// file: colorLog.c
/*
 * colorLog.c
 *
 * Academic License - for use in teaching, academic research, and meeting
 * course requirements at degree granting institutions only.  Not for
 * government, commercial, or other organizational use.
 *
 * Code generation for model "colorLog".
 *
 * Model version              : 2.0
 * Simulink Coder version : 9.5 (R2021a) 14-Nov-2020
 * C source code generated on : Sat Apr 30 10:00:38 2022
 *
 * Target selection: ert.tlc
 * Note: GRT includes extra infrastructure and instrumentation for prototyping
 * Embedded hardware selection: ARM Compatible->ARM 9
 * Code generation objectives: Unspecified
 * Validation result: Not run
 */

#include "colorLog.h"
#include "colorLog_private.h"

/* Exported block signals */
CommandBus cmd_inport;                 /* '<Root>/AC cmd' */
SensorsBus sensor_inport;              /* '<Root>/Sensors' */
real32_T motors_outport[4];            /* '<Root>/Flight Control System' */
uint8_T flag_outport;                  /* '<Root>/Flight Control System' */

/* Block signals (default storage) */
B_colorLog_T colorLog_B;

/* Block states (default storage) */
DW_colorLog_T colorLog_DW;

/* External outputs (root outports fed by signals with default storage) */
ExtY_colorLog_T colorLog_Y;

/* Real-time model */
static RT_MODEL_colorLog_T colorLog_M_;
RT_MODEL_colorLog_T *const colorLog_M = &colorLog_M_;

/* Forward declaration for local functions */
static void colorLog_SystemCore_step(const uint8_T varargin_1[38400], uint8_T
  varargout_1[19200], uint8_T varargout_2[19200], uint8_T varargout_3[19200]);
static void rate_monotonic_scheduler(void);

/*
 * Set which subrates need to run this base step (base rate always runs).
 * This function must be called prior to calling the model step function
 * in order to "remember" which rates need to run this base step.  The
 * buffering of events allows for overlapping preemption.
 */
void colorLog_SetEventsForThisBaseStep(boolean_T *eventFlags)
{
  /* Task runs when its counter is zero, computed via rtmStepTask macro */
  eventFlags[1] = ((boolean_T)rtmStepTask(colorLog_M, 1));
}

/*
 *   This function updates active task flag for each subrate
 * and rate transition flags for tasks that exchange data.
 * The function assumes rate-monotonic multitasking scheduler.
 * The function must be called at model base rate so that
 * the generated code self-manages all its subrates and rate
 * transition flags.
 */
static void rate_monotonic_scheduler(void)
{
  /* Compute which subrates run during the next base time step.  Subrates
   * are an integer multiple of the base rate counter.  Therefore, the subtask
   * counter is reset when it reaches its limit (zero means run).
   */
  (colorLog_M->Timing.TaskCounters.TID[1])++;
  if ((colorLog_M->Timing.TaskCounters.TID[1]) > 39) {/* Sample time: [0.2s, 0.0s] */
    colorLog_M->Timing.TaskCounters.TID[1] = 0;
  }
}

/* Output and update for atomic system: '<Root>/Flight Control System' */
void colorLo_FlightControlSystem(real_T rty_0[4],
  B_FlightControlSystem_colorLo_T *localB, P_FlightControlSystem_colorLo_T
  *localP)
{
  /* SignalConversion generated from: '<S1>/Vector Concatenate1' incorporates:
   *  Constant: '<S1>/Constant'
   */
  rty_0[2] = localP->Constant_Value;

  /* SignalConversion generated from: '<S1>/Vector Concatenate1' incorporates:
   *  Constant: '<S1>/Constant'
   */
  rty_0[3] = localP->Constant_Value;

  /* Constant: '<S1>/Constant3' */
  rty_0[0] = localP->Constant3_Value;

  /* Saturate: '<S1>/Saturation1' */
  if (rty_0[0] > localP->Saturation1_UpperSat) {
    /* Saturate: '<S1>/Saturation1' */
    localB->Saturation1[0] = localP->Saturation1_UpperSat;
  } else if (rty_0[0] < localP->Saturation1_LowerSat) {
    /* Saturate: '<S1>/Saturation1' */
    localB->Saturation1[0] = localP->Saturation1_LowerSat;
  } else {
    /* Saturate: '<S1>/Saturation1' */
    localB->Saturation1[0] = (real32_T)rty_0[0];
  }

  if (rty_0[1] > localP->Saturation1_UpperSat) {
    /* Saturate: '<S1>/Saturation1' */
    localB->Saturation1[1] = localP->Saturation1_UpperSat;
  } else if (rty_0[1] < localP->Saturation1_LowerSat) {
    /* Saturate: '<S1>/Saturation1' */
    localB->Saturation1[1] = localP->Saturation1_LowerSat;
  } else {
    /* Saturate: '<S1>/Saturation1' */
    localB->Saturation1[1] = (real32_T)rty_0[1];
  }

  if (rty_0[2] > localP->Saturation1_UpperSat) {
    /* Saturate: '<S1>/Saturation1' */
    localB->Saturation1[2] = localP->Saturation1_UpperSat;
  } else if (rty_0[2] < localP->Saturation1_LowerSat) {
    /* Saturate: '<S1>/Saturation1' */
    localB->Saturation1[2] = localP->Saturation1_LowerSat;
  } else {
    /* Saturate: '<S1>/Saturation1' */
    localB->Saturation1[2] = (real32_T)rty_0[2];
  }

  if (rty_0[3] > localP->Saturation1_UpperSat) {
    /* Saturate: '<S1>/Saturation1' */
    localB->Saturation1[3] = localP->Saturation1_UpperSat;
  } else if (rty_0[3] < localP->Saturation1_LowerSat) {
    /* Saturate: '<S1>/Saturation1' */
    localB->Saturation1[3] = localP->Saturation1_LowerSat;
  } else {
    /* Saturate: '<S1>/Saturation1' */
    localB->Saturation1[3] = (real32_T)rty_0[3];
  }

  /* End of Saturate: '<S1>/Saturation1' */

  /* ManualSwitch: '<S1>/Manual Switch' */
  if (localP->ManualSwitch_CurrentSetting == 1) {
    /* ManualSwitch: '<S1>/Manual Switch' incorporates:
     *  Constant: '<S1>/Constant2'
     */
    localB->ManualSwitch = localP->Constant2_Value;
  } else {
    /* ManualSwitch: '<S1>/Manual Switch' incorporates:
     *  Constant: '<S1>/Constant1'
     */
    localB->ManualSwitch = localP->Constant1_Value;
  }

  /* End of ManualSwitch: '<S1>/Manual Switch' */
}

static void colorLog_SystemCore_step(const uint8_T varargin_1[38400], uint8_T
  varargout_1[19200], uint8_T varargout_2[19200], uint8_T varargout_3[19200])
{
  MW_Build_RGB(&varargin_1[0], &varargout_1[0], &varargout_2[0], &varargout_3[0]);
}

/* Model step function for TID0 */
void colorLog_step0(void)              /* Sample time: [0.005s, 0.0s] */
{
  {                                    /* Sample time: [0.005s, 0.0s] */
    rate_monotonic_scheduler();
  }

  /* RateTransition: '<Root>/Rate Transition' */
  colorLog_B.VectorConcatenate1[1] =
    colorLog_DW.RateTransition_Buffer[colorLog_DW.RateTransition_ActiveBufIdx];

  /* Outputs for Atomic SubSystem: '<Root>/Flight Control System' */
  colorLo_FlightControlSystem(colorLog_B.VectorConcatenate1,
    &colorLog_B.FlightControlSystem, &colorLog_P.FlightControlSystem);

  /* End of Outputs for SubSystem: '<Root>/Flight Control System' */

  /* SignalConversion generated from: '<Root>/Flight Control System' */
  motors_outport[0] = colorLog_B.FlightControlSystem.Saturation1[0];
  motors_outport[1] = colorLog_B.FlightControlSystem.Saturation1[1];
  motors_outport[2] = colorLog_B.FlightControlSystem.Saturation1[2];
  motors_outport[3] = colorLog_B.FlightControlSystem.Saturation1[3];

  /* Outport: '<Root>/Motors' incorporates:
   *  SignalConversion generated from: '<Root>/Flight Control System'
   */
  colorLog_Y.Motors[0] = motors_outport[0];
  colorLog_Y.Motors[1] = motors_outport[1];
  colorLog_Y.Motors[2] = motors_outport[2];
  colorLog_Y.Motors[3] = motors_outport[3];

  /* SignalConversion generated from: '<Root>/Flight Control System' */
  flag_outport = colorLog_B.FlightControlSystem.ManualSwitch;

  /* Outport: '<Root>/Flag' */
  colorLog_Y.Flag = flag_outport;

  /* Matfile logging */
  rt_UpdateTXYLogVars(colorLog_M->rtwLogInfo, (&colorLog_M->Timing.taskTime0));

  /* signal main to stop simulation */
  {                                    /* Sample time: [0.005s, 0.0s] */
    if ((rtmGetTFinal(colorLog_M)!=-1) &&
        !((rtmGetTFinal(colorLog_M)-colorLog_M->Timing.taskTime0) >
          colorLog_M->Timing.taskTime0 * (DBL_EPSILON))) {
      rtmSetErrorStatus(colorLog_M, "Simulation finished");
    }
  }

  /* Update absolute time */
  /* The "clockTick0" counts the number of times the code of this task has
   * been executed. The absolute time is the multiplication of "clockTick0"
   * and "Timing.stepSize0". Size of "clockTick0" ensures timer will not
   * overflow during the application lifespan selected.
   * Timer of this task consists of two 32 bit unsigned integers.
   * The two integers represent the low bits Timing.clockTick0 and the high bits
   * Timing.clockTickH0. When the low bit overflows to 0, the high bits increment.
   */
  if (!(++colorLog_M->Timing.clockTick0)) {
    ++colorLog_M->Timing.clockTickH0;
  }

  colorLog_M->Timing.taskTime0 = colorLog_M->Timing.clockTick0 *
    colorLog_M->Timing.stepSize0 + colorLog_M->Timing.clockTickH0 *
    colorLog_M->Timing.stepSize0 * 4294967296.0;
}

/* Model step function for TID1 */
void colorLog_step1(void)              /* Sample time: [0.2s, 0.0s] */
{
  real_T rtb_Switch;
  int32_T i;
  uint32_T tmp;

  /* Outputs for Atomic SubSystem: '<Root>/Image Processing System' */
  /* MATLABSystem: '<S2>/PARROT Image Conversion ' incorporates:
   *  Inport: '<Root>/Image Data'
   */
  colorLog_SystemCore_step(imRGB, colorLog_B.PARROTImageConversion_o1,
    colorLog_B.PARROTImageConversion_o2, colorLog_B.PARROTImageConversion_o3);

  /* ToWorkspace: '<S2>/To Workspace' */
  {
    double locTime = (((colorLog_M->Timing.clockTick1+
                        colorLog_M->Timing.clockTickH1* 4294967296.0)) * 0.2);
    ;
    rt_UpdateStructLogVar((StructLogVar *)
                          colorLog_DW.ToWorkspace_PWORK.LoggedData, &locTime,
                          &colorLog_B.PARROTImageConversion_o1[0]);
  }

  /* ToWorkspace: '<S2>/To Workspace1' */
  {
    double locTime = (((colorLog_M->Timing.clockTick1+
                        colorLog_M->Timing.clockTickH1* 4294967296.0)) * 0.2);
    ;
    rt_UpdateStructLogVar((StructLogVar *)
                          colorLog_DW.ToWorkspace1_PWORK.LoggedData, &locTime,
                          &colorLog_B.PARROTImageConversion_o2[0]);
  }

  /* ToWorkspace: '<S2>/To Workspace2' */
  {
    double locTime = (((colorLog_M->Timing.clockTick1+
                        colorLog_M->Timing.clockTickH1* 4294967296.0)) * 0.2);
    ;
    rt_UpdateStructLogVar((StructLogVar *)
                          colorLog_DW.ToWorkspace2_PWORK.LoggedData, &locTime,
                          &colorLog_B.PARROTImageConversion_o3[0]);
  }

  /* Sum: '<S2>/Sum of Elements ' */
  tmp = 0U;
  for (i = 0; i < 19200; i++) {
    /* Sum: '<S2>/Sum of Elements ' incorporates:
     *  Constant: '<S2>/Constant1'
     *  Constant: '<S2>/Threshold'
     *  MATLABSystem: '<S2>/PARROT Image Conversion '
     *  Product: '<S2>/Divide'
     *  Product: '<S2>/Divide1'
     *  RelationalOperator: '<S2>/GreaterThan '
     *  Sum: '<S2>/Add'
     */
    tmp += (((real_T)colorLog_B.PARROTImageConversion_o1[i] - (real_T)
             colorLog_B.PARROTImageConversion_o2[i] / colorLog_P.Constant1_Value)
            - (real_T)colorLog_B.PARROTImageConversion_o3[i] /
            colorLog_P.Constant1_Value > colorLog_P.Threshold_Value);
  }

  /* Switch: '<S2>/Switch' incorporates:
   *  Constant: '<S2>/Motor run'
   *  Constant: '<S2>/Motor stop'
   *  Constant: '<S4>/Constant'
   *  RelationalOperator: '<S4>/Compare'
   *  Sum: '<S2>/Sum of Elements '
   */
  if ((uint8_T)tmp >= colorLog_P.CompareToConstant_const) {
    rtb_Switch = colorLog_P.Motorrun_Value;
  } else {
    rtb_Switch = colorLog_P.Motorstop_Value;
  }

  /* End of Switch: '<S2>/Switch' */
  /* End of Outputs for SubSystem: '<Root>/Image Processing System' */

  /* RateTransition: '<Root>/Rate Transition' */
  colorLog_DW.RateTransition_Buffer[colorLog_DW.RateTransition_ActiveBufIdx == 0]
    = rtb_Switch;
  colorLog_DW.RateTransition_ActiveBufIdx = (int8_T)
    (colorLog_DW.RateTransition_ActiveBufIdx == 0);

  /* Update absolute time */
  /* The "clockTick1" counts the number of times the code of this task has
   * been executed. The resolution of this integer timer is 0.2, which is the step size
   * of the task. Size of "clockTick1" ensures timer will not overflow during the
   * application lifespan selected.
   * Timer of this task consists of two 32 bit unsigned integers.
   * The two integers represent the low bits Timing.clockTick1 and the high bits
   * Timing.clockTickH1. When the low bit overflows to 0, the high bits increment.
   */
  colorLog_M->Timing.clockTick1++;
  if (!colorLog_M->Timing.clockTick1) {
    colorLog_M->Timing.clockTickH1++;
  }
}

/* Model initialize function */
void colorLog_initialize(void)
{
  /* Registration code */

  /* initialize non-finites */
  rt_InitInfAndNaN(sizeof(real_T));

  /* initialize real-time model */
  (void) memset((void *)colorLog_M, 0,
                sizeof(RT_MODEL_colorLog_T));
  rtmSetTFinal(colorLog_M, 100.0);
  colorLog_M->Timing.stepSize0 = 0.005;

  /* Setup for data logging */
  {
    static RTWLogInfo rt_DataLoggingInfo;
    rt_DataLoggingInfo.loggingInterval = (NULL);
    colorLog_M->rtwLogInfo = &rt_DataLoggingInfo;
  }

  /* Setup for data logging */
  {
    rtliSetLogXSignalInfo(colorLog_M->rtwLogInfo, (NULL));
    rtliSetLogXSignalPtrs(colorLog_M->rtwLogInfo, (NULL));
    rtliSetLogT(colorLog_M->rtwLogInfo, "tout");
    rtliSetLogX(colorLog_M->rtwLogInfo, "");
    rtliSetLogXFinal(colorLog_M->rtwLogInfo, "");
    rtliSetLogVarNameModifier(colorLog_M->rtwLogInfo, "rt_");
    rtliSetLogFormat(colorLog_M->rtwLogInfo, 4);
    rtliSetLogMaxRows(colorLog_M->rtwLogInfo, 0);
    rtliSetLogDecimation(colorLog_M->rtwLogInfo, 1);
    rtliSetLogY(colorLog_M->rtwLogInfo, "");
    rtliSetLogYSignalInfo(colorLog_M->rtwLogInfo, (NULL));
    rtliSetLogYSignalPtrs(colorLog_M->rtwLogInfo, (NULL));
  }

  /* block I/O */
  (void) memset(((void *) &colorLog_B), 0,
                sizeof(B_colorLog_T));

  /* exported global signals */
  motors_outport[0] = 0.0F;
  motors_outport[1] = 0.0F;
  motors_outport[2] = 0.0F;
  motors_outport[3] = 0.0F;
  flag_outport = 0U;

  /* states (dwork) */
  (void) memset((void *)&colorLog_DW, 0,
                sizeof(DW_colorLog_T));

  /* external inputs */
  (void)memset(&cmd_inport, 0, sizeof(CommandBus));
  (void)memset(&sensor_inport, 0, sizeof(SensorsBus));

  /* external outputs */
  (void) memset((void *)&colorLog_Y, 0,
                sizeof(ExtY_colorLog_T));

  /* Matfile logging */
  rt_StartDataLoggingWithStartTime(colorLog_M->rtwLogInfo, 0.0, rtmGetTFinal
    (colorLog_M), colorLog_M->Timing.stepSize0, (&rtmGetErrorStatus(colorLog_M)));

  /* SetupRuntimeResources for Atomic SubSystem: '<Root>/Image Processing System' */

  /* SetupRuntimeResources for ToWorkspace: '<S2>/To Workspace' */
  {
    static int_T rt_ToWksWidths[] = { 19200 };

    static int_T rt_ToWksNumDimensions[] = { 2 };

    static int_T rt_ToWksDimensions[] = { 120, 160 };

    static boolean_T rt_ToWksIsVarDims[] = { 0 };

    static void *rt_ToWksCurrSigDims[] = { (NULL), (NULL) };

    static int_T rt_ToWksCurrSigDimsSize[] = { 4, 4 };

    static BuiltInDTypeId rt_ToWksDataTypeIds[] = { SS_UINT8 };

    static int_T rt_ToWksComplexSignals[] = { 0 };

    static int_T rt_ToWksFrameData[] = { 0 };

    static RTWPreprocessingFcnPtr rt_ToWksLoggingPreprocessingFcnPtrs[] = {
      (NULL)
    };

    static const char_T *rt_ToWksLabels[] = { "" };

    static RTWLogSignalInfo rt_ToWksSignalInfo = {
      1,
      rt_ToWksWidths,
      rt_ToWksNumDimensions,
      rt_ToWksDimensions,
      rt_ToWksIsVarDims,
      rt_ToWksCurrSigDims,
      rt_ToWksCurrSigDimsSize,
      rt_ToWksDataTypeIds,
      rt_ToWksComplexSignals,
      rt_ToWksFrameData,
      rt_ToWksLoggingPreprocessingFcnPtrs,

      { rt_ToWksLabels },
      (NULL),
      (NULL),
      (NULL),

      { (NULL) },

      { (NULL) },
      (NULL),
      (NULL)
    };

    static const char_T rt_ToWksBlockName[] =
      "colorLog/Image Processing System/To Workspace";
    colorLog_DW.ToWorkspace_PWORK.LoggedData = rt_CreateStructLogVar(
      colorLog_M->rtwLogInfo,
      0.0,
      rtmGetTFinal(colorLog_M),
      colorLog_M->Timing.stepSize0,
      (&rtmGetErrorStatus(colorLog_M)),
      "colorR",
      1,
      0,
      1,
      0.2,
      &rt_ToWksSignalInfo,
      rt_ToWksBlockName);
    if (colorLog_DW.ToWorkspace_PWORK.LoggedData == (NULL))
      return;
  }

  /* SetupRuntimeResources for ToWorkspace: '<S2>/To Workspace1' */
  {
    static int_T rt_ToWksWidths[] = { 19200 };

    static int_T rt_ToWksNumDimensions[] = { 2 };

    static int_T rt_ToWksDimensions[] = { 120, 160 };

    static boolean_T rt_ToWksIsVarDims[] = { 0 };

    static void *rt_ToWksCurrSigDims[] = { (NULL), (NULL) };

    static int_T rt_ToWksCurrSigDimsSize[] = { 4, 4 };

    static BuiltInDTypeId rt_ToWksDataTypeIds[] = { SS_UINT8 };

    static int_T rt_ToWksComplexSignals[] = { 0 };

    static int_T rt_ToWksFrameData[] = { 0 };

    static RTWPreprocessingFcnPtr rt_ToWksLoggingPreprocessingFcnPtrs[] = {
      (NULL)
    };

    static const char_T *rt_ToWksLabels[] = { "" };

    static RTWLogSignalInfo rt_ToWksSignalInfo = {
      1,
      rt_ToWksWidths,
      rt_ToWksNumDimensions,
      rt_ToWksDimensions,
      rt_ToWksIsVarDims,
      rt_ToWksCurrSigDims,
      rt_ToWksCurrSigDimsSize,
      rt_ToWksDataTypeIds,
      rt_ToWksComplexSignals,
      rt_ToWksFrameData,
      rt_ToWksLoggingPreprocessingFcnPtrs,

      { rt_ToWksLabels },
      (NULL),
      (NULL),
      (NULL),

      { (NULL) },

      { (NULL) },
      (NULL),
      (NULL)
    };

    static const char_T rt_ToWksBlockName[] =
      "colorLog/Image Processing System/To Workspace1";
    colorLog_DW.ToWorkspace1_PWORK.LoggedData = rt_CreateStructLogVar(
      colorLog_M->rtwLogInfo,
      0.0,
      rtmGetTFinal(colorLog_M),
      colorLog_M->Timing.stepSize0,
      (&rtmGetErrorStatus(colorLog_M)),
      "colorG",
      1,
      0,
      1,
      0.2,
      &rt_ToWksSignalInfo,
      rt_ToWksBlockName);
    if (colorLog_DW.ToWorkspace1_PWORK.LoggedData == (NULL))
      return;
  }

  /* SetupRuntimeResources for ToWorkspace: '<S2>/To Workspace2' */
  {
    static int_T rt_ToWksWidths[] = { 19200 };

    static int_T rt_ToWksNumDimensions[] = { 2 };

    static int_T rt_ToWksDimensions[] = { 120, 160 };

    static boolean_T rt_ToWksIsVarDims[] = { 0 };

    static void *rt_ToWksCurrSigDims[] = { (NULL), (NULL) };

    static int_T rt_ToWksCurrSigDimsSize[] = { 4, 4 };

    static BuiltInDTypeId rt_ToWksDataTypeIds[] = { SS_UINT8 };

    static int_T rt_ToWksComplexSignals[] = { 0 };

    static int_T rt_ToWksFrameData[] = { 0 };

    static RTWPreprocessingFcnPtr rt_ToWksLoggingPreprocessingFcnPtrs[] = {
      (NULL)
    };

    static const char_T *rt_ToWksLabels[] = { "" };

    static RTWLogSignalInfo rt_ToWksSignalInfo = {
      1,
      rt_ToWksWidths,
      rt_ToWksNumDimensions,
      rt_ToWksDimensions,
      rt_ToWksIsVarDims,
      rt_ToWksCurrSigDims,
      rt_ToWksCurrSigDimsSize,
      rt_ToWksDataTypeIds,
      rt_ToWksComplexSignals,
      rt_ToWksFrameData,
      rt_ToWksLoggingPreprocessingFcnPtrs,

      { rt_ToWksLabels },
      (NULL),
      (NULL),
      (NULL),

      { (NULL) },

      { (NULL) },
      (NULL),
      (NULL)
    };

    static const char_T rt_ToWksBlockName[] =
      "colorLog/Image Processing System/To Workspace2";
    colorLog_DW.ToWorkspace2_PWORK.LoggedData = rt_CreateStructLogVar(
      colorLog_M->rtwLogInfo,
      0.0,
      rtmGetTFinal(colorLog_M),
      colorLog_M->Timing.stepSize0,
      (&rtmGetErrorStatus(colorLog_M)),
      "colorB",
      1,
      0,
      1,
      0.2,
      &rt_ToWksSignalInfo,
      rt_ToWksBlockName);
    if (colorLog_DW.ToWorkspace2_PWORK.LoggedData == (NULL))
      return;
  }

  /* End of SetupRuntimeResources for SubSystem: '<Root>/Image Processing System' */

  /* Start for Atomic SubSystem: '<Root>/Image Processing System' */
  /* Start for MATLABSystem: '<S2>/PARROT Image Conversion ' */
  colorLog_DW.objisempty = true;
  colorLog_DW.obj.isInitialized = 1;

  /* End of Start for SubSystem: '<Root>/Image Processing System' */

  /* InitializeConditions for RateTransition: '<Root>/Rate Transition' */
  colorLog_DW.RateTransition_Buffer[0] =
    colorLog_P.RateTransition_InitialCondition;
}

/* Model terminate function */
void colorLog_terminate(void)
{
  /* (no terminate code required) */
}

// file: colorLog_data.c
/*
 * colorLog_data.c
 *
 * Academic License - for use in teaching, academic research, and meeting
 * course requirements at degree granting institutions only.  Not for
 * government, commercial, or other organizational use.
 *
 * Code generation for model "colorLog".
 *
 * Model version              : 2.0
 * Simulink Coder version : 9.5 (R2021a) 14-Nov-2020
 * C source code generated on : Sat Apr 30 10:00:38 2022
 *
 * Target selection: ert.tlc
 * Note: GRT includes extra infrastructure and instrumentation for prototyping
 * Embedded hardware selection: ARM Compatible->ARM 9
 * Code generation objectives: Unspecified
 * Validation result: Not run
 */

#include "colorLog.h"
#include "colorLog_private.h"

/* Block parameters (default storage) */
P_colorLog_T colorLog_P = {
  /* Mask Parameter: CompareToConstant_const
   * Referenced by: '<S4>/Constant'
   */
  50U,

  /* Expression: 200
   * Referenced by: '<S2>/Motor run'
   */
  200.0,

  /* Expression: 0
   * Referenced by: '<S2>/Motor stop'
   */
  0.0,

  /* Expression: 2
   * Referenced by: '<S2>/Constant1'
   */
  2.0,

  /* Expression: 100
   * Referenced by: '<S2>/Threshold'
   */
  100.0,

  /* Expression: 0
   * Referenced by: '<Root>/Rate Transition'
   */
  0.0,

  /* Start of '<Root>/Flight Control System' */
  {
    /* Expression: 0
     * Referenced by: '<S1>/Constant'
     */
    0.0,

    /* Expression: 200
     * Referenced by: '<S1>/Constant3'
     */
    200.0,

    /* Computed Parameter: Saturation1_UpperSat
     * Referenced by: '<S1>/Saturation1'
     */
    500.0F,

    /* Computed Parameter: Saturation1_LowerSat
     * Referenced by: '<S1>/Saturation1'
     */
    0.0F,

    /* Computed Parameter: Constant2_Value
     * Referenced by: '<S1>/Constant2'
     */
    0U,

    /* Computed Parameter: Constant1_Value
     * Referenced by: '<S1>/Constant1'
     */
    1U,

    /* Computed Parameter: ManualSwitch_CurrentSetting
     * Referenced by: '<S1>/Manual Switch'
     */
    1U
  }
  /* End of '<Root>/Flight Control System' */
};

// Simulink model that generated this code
simulink model "colorLog"  (R2021a)
settings: Solver=FixedStepAuto  StartTime=0.0  StopTime=100  RelTol=1e-3  EnableMultiTasking=on
InitFcn:
  | load('BusDefinitions.mat')
  | codertarget.parrot.internal.checkImageBlocks(gcs)
undefined symbols (not defined in the file or in its folder): codertarget, Ts
libraries: simulink x1, parrotlib x1

== system colorLog ==
  note: Model your control logic inside this subsystem
      | using the Sensor values and Vision-based Data,
      | and output the Motor values.
      | This block is running at 5ms.
      | DO NOT change the sample time of the block.
  note: DO NOT MODIFY these output ports
      | and signal properties.
      |
      |
      |
      |
      |
      | Always ensure the 'Motors' outport
      | is fed with a 1 x 4 single vector.
      |
      |
      |
      |
      |
      | Always ensure the 'Flag' outport is
      | fed with a 1 x 1 uint8 value.
  note: DO NOT MODIFY these input
      | ports and signal properties.
  note: Copyright 2018-2020 The MathWorks, Inc.
  note: Getting started with vision on Parrot Minidrones
  note: DO NOT MODIFY the input port and
      | signal properties.
  note: Model your image processing algorithm inside this
      | subsystem by using the image from the camera
      | and additional logic to process the data.
      | This subsystem is running at 200ms.
      | DO NOT change the sample time of the subsystem.
  AC cmd : Inport  OutDataTypeStr=Bus: CommandBus  BusOutputAsStruct=on
  Sensors : Inport  Port=2  OutDataTypeStr=Bus: SensorsBus  BusOutputAsStruct=on
  Image Data : Inport  Tag=IP_IN  InitFcn=codertarget.parrot.internal.inportCallback(gcb);  Port=3  OutDataTypeStr=uint8  PortDimensions=[4 9600]  BusOutputAsStruct=on
  Flight Control System : Subsystem  InitFcn=codertarget.parrot.internal.fcsSubsystemCallback(gcb);  TreatAsAtomicUnit=on  SystemSampleTime=Ts
  Image Processing System : Subsystem  Tag=IP_SUB  InitFcn=codertarget.parrot.internal.ipSubsystemCallback(gcb);  TreatAsAtomicUnit=on  SystemSampleTime=40*Ts  RTWFcnName=ImageFunction
  Rate Transition : RateTransition  Deterministic=off
  Motors : Outport  OutDataTypeStr=single  PortDimensions=[1 4]  VectorParamsAs1DForOutWhenUnconnected=off
  Flag : Outport  Port=2  OutDataTypeStr=uint8  PortDimensions=1  VectorParamsAs1DForOutWhenUnconnected=off
  wires:
  Flight Control System/1(Motors) -> Motors/1  "Motor"
  AC cmd/1 -> Flight Control System/1(AC cmd)  "Command"
  Sensors/1 -> Flight Control System/2(Sensors)  "Sensor_values"
  Flight Control System/2(Flag) -> Flag/1  "flag"
  Image Data/1 -> Image Processing System/1(Image Data)  "Y1UY2V"
  Rate Transition/1 -> Flight Control System/3(" Vision-based Data")
  Image Processing System/1(" Vision-based Data") -> Rate Transition/1

== system colorLog/Flight Control System ==
  note: The 'Motors' outport is fed with the speed values of the 4 motors.
  note: Model an error condition and feed the value to 'Flag' outport block.
      | Value '0' indicates that all the flight conditions are good and the drone
      | can continue its flight.
      | A non-zero value indicates an error condition, and stops the drone
      | flight.
  note: The SensorsBus contains data from sensors like
      | accelerometer, gyroscope, ultrasonic, pressure,
      | and optical flow data.
  AC cmd : Inport
  Sensors : Inport  Port=2
  " Vision-based Data" : Inport  Port=3
  Bus Selector : BusSelector  OutputSignals=controlModePosVSOrient,pos_ref,takeoff_flag,orient_ref,live_time_ticks
  Bus Selector1 : BusSelector  OutputSignals=VisionSensors,HALSensors,SensorCalibration
  Constant : Constant  Value=0
  Constant1 : Constant  OutDataTypeStr=uint8
  Constant2 : Constant  Value=0  OutDataTypeStr=uint8
  Constant3 : Constant  Value=200
  Manual Switch : ManualSwitch
  Saturation1 : Saturate  UpperLimit=500  LowerLimit=0  OutDataTypeStr=single
  Subsystem : Subsystem
  Terminator{,1,3..7,9..18} (17 alike) : Terminator
  Vector Concatenate1 : Concatenate  NumInputs=4
  Motors : Outport  VectorParamsAs1DForOutWhenUnconnected=off
  Flag : Outport  Port=2  VectorParamsAs1DForOutWhenUnconnected=off
  wires:
  AC cmd/1 -> Bus Selector/1
  Sensors/1 -> Bus Selector1/1
  Bus Selector/1 -> Terminator3/1  "<controlModePosVSOrient>"
  Bus Selector/2 -> Terminator4/1  "<pos_ref>"
  Bus Selector/3 -> Terminator5/1  "<takeoff_flag>"
  Bus Selector/4 -> Terminator6/1  "<orient_ref>"
  Bus Selector/5 -> Terminator7/1  "<live_time_ticks>"
  Manual Switch/1 -> Flag/1
  Constant2/1 -> Manual Switch/1
  Constant1/1 -> Manual Switch/2
  Vector Concatenate1/1 -> Saturation1/1
  Saturation1/1 -> Motors/1
  Bus Selector1/1 -> Subsystem/1(<VisionSensors>)  "<VisionSensors>"
  Bus Selector1/2 -> Subsystem/2(<HALSensors>)  "<HALSensors>"
  Bus Selector1/3 -> Terminator/1  "<SensorCalibration>"
  Subsystem/1(OF_data) -> Terminator1/1
  Subsystem/2(ddx) -> Terminator9/1
  Subsystem/3(ddy) -> Terminator10/1
  Subsystem/4(ddz) -> Terminator11/1
  Subsystem/5(p) -> Terminator12/1
  Subsystem/7(r) -> Terminator14/1
  Subsystem/8(prs) -> Terminator15/1
  Subsystem/9(altitude_sonar) -> Terminator16/1
  Subsystem/10(vbat_V) -> Terminator17/1
  Subsystem/11(vbat_percentage) -> Terminator18/1
  Subsystem/6(q) -> Terminator13/1
  Constant/1 -> Vector Concatenate1/3, Vector Concatenate1/4
  " Vision-based Data"/1 -> Vector Concatenate1/2
  Constant3/1 -> Vector Concatenate1/1

== system colorLog/Image Processing System ==
  Image Data : Inport
  Add : Sum  Inputs=+--
  "Compare To Constant " : simulink/Logic and Bit Operations/Compare To Constant  relop=>=  const=50  OutDataTypeStr=boolean
  Constant1 : Constant  Value=2
  Divide : Product  Inputs=*/
  Divide1 : Product  Inputs=*/
  "GreaterThan " : RelationalOperator  Operator=>  OutDataTypeStr=boolean  RndMeth=Simplest
  Motor run : Constant  Value=200
  Motor stop : Constant  Value=0
  "PARROT Image Conversion " : parrotlib/PARROT Image Conversion  Tag=IP_FORMAT  ImageFormat=RGB  R=on  Y=on  G=on  U=on  B=on  V=on
  "Sum of Elements " : Sum  Inputs=+
  Switch : Switch  Criteria=u2 > Threshold
  Threshold : Constant  Value=100
  " Vision-based Data" : Outport  VectorParamsAs1DForOutWhenUnconnected=off
  wires:
  "PARROT Image Conversion "/1 -> Add/1
  Divide1/1 -> Add/3
  "Sum of Elements "/1 -> "Compare To Constant "/1
  Switch/1 -> " Vision-based Data"/1
  "Compare To Constant "/1 -> Switch/2
  "PARROT Image Conversion "/3 -> Divide1/1
  Image Data/1 -> "PARROT Image Conversion "/1
  "PARROT Image Conversion "/2 -> Divide/1
  Threshold/1 -> "GreaterThan "/2
  Motor run/1 -> Switch/1
  Constant1/1 -> Divide1/2, Divide/2
  Add/1 -> "GreaterThan "/1
  "GreaterThan "/1 -> "Sum of Elements "/1
  Divide/1 -> Add/2
  Motor stop/1 -> Switch/3

== system colorLog/Flight Control System/Subsystem ==
  <VisionSensors> : Inport
  <HALSensors> : Inport  Port=2
  Bus Selector1 : BusSelector  OutputSignals=opticalFlow_data
  Bus Selector2 : BusSelector  OutputSignals=HAL_acc_SI,HAL_gyro_SI,HAL_pressure_SI,HAL_ultrasound_SI,HAL_vbat_SI
  Bus Selector3 : BusSelector  OutputSignals=x,y,z
  Bus Selector4 : BusSelector  OutputSignals=x,y,z
  Bus Selector5 : BusSelector  OutputSignals=pressure
  Bus Selector6 : BusSelector  OutputSignals=altitude
  Bus Selector7 : BusSelector  OutputSignals=vbat_V,vbat_percentage
  OF_data : Outport  VectorParamsAs1DForOutWhenUnconnected=off
  ddx : Outport  Port=2  VectorParamsAs1DForOutWhenUnconnected=off
  ddy : Outport  Port=3  VectorParamsAs1DForOutWhenUnconnected=off
  ddz : Outport  Port=4  VectorParamsAs1DForOutWhenUnconnected=off
  p : Outport  Port=5  VectorParamsAs1DForOutWhenUnconnected=off
  q : Outport  Port=6  VectorParamsAs1DForOutWhenUnconnected=off
  r : Outport  Port=7  VectorParamsAs1DForOutWhenUnconnected=off
  prs : Outport  Port=8  VectorParamsAs1DForOutWhenUnconnected=off
  altitude_sonar : Outport  Port=9  VectorParamsAs1DForOutWhenUnconnected=off
  vbat_V : Outport  Port=10  VectorParamsAs1DForOutWhenUnconnected=off
  vbat_percentage : Outport  Port=11  VectorParamsAs1DForOutWhenUnconnected=off
  wires:
  <VisionSensors>/1 -> Bus Selector1/1
  <HALSensors>/1 -> Bus Selector2/1
  Bus Selector1/1 -> OF_data/1  "<opticalFlow_data>"
  Bus Selector2/1 -> Bus Selector3/1  "<HAL_acc_SI>"
  Bus Selector2/2 -> Bus Selector4/1  "<HAL_gyro_SI>"
  Bus Selector2/3 -> Bus Selector5/1  "<HAL_pressure_SI>"
  Bus Selector2/4 -> Bus Selector6/1  "<HAL_ultrasound_SI>"
  Bus Selector2/5 -> Bus Selector7/1  "<HAL_vbat_SI>"
  Bus Selector3/1 -> ddx/1  "<x>"
  Bus Selector3/2 -> ddy/1  "<y>"
  Bus Selector3/3 -> ddz/1  "<z>"
  Bus Selector4/2 -> q/1  "<y>"
  Bus Selector4/1 -> p/1  "<x>"
  Bus Selector4/3 -> r/1  "<z>"
  Bus Selector5/1 -> prs/1  "<pressure>"
  Bus Selector6/1 -> altitude_sonar/1  "<altitude>"
  Bus Selector7/1 -> vbat_V/1  "<vbat_V>"
  Bus Selector7/2 -> vbat_percentage/1  "<vbat_percentage>"
